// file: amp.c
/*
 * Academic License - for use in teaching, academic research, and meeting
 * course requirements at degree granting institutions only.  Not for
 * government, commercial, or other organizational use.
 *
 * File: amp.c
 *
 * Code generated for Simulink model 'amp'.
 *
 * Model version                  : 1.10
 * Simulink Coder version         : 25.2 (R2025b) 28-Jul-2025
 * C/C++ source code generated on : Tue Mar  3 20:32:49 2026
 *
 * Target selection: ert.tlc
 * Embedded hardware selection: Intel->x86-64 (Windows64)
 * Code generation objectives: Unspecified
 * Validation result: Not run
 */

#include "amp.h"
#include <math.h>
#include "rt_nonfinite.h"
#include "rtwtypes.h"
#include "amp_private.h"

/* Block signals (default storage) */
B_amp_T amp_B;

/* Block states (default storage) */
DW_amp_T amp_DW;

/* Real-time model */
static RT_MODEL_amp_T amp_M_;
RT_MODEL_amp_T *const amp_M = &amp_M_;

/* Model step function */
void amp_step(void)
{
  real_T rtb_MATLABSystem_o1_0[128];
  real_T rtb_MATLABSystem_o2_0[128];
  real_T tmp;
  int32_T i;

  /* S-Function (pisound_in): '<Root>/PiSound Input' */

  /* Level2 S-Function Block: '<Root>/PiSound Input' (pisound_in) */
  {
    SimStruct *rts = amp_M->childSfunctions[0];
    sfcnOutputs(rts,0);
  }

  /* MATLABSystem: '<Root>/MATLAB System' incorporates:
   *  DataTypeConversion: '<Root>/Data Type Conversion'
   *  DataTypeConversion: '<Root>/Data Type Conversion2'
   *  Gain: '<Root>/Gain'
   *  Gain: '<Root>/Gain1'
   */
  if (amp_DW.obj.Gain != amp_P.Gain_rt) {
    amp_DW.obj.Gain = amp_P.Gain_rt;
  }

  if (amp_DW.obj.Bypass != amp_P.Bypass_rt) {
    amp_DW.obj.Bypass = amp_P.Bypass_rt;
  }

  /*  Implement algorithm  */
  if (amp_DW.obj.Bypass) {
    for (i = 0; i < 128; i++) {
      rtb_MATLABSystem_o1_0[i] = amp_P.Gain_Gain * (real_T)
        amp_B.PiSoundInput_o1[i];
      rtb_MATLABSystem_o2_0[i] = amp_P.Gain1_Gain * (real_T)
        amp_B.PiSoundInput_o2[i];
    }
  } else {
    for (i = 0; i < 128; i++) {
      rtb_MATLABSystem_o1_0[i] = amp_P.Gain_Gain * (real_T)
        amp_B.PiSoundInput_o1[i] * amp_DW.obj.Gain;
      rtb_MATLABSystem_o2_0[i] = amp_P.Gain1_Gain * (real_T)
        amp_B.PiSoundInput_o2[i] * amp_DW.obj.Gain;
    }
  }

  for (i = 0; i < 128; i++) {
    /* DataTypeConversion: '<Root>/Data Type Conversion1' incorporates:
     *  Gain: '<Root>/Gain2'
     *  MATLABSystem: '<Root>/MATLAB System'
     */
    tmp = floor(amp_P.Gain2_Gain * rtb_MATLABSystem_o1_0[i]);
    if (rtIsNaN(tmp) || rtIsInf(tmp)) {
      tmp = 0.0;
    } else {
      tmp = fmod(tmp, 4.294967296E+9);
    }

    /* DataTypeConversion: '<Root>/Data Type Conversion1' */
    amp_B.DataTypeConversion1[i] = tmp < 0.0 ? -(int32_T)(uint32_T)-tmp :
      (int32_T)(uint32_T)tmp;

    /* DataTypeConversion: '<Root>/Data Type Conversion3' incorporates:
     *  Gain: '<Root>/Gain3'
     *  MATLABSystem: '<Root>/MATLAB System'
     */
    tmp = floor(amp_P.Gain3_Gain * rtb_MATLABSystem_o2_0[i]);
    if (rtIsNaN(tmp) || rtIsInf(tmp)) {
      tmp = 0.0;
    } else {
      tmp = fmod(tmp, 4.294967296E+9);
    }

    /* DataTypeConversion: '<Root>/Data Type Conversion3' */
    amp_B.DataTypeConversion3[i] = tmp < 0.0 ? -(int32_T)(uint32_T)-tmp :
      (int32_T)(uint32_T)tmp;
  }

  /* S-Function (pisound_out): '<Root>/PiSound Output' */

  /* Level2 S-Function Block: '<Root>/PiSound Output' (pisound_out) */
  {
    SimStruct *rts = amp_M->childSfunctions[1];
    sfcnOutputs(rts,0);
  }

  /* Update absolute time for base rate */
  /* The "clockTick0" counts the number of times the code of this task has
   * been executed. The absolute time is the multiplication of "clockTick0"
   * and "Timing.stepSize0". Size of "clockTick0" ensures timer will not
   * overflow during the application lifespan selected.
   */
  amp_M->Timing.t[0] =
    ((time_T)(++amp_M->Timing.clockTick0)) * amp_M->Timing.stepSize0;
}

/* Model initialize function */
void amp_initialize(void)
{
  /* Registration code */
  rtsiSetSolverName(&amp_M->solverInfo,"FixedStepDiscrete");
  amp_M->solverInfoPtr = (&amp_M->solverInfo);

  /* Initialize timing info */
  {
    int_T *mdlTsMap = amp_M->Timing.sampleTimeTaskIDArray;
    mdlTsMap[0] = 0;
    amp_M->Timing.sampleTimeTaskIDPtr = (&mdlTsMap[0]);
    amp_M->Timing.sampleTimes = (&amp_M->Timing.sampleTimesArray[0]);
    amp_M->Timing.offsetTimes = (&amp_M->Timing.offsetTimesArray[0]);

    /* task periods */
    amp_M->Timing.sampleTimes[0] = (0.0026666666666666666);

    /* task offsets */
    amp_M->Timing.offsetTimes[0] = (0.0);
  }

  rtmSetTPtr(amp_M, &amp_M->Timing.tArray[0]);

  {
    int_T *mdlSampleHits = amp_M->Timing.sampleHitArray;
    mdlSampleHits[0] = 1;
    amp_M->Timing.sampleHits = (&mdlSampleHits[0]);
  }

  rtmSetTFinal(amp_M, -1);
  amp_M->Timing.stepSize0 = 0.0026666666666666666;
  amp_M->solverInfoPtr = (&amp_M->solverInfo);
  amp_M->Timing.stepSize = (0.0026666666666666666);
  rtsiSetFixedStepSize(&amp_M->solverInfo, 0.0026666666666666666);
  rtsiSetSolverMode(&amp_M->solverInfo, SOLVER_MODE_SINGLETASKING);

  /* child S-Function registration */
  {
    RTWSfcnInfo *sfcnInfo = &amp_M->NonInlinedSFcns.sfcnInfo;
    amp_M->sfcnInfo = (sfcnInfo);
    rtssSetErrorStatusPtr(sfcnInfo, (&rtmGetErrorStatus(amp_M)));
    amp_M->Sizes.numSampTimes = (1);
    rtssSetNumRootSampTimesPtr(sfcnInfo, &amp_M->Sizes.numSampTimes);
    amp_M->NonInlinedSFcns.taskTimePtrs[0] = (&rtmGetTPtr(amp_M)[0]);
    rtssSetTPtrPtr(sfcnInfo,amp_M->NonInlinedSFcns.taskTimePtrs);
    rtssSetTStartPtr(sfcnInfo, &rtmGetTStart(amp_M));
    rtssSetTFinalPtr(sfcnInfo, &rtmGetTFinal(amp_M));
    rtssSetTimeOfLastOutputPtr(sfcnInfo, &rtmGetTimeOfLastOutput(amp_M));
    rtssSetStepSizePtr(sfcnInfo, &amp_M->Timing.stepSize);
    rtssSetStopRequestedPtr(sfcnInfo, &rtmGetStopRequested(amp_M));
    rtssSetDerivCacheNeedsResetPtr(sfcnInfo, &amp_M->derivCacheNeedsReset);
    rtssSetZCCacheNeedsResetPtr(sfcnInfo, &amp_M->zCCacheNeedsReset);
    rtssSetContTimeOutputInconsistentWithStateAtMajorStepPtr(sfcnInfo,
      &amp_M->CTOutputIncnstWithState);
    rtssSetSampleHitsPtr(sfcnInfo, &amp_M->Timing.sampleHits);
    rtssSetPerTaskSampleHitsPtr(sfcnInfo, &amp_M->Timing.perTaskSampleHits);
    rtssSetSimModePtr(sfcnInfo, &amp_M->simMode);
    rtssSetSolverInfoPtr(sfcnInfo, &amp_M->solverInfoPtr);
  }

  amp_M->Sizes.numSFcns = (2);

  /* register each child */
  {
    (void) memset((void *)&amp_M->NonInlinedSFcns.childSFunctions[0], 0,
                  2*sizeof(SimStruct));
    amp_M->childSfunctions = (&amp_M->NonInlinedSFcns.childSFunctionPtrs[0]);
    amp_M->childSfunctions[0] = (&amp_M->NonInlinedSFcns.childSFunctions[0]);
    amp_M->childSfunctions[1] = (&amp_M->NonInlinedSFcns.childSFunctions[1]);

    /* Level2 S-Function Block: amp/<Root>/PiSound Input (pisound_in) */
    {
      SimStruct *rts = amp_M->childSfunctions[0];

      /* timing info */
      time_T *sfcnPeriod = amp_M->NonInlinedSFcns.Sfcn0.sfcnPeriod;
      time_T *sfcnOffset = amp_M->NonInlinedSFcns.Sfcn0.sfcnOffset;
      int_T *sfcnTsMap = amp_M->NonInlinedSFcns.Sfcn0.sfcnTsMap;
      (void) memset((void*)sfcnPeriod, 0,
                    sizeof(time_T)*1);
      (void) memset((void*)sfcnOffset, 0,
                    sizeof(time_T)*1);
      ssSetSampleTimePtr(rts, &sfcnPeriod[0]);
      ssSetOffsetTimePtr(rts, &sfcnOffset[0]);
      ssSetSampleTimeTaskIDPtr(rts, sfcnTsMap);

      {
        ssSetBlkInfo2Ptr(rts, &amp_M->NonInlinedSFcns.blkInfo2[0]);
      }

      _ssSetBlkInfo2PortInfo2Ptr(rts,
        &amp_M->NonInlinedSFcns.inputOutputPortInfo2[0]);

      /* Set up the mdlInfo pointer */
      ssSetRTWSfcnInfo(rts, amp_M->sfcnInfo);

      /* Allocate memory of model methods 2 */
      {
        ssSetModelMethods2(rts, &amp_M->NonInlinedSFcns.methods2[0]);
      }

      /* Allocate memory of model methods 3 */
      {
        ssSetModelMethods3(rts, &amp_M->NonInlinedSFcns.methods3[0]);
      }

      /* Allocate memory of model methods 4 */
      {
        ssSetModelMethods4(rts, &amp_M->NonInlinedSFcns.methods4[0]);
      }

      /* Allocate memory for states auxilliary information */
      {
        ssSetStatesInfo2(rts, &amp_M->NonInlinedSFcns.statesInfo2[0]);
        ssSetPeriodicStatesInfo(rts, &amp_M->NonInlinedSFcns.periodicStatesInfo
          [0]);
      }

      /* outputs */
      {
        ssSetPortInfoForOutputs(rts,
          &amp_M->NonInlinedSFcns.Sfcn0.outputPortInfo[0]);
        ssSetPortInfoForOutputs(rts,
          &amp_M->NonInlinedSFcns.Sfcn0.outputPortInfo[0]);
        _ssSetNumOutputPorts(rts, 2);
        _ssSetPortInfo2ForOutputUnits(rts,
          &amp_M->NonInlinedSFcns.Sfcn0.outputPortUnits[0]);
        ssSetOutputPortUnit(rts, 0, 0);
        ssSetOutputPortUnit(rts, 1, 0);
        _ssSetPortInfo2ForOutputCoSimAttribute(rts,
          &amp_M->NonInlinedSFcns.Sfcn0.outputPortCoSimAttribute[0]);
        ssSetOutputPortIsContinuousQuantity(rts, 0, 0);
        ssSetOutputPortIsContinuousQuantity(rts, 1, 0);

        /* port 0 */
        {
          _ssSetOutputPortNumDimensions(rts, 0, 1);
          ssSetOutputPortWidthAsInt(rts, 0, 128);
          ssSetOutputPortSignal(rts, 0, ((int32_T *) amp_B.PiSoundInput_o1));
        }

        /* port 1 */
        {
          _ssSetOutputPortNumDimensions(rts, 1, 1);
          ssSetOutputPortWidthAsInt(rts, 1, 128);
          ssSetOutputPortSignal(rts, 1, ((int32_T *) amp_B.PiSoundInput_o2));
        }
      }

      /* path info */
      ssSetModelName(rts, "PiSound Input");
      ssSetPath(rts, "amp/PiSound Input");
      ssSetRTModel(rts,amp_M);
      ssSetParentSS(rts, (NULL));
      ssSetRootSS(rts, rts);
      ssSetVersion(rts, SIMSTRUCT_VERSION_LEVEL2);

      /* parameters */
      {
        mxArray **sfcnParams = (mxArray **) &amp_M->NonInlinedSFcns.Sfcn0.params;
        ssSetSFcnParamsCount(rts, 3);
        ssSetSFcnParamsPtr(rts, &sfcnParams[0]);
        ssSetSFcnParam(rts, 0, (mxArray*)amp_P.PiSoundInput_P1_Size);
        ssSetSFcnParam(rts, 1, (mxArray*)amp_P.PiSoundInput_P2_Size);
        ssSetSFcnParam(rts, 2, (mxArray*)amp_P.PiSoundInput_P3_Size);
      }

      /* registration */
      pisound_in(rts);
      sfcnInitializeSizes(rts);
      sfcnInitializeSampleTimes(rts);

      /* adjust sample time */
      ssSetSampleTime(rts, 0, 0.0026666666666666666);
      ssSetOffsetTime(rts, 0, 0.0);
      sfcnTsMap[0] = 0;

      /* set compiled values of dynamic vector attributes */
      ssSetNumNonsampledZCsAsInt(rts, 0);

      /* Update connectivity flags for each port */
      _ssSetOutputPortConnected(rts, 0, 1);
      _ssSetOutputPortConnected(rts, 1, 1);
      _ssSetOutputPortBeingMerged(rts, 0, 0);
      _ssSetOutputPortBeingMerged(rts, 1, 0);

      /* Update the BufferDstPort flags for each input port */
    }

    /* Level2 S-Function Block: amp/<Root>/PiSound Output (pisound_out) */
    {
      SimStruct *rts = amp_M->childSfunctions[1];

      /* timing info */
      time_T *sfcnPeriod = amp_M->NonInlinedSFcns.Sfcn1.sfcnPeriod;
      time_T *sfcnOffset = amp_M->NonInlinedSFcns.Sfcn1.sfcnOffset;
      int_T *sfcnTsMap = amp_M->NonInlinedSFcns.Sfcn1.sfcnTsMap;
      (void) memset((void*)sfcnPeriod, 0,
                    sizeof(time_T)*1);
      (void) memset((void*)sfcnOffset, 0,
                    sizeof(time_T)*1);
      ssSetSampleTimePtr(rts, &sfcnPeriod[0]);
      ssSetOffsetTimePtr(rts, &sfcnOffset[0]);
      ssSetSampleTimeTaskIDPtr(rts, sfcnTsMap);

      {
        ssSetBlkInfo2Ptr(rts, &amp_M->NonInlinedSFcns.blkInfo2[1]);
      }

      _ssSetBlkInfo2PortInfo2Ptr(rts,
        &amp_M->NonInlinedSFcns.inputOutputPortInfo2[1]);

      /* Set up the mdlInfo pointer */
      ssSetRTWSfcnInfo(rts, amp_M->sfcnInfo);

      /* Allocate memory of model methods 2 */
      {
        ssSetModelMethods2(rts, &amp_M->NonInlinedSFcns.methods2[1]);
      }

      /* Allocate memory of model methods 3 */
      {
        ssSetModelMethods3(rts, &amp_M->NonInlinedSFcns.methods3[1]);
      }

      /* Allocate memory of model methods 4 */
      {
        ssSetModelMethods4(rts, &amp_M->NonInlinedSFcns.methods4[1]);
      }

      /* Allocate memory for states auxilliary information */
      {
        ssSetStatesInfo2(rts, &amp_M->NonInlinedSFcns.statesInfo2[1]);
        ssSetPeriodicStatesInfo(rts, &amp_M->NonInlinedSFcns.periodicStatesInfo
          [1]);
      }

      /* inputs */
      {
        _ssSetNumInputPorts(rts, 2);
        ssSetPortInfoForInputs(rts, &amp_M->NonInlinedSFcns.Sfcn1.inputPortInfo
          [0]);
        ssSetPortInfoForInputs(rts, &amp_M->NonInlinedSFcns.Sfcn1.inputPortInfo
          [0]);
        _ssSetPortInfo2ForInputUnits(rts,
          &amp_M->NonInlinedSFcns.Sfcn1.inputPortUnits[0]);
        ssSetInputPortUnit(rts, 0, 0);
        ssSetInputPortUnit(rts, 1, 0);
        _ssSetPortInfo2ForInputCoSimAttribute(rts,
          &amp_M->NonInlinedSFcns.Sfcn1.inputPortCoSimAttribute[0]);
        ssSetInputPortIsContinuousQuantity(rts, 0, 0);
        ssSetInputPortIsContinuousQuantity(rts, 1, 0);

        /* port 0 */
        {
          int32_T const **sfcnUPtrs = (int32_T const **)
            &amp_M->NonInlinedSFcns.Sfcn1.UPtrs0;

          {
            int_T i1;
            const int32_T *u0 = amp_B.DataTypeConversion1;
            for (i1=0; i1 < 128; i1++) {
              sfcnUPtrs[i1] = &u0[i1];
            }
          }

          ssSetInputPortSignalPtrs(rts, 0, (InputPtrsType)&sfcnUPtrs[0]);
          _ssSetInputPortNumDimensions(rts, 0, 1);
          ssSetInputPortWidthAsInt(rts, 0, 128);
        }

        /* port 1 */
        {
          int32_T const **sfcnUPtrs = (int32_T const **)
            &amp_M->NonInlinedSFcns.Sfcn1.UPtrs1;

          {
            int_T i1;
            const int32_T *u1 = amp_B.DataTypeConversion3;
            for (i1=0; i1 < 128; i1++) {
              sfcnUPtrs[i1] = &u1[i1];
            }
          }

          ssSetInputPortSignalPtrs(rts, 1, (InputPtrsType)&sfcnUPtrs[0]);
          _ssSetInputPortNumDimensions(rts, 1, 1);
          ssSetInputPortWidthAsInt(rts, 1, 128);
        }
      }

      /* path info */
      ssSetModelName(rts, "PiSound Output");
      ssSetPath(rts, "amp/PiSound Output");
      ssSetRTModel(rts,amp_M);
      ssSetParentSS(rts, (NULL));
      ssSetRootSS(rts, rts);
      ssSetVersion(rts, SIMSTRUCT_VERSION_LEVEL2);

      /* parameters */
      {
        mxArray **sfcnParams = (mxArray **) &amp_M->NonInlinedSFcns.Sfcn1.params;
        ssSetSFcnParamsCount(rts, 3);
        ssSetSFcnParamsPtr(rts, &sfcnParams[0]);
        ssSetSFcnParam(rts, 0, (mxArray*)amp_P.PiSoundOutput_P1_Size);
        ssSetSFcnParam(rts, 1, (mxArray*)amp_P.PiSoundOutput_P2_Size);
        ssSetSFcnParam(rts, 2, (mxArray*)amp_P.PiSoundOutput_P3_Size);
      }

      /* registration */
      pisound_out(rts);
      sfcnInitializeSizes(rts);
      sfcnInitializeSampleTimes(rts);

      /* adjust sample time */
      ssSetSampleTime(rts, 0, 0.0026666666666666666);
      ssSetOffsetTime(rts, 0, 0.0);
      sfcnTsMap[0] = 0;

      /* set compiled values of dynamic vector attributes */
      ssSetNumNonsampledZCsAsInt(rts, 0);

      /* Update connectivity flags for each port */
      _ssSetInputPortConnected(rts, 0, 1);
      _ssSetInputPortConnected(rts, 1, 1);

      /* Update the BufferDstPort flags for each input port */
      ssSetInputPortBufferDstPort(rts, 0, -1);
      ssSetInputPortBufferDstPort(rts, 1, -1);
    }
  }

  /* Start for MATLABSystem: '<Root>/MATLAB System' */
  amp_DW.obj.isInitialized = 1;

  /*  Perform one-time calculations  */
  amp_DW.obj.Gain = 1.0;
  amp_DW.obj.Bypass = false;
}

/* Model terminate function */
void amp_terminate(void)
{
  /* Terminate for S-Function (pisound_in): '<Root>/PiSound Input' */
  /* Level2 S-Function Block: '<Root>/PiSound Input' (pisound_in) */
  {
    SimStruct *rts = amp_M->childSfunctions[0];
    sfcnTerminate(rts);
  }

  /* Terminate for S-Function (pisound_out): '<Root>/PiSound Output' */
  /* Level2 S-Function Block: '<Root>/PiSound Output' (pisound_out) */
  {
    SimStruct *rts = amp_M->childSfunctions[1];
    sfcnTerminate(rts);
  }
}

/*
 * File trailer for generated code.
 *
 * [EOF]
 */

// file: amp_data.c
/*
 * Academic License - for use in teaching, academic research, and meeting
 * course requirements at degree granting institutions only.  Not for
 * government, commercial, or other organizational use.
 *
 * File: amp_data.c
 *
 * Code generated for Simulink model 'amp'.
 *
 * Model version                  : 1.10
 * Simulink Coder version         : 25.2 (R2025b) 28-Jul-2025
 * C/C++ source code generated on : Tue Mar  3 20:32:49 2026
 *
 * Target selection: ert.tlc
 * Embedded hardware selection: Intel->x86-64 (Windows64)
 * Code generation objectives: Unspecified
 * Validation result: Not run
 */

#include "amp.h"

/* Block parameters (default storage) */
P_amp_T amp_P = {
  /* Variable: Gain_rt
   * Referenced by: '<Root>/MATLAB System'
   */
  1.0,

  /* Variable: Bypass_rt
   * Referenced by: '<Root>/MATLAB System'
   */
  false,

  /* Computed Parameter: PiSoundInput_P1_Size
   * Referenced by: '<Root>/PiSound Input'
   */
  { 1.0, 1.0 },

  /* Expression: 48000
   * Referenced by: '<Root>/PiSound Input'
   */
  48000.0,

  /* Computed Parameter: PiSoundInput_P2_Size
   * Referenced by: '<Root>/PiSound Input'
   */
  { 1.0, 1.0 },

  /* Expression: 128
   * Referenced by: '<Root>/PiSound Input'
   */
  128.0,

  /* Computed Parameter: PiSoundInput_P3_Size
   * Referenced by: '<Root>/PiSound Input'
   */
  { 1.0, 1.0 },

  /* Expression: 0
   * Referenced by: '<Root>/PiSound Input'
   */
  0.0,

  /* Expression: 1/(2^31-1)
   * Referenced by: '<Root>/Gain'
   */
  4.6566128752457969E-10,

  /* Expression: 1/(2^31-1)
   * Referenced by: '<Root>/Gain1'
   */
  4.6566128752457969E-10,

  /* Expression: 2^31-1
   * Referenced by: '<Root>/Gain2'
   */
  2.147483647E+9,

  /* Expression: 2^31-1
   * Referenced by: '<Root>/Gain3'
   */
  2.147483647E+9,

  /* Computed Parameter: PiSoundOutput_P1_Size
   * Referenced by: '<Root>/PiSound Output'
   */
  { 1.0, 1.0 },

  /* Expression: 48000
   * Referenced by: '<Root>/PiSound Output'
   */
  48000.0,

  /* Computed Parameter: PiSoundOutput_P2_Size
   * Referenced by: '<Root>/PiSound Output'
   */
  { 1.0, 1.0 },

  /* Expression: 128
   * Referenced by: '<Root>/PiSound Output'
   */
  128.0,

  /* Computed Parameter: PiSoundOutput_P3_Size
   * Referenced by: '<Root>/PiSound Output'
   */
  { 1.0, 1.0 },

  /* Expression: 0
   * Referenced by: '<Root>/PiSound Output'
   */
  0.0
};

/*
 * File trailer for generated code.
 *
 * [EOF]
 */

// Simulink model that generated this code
simulink model "amp"  (R2025b)
settings: Solver=FixedStepDiscrete  StartTime=0.0  StopTime=inf  RelTol=1e-3
model workspace (MATLAB code in the model file):
  | Gain_rt = Simulink.Parameter(1.0);
  | Bypass_rt = Simulink.Parameter(false);

== system amp ==
  Data Type Conversion : DataTypeConversion  OutDataTypeStr=double  SaturateOnIntegerOverflow=off  RndMeth=Floor
  Data Type Conversion1 : DataTypeConversion  OutDataTypeStr=int32  SaturateOnIntegerOverflow=off  RndMeth=Floor
  Data Type Conversion2 : DataTypeConversion  OutDataTypeStr=double  SaturateOnIntegerOverflow=off  RndMeth=Floor
  Data Type Conversion3 : DataTypeConversion  OutDataTypeStr=int32  SaturateOnIntegerOverflow=off  RndMeth=Floor
  Gain : Gain  Gain=1/(2^31-1)
  Gain1 : Gain  Gain=1/(2^31-1)
  Gain2 : Gain  Gain=2^31-1
  Gain3 : Gain  Gain=2^31-1
  MATLAB System : MATLABSystem  System=amp_sys  Fs=48000  Gain=Gain_rt  Bypass=Bypass_rt  SimulateUsing=Code generation
  PiSound Input : S-Function  FunctionName=pisound_in  Parameters=48000, 128, 0  SFunctionDeploymentMode=off  EnableBusSupport=off
  PiSound Output : S-Function  FunctionName=pisound_out  Parameters=48000, 128, 0  SFunctionDeploymentMode=off  EnableBusSupport=off
  wires:
  PiSound Input/1 -> Data Type Conversion/1
  PiSound Input/2 -> Data Type Conversion2/1
  Data Type Conversion1/1 -> PiSound Output/1
  Data Type Conversion3/1 -> PiSound Output/2
  Gain2/1 -> Data Type Conversion1/1
  Gain3/1 -> Data Type Conversion3/1
  Data Type Conversion/1 -> Gain/1
  Data Type Conversion2/1 -> Gain1/1
  Gain/1 -> MATLAB System/1
  MATLAB System/1 -> Gain2/1
  Gain1/1 -> MATLAB System/2
  MATLAB System/2 -> Gain3/1
